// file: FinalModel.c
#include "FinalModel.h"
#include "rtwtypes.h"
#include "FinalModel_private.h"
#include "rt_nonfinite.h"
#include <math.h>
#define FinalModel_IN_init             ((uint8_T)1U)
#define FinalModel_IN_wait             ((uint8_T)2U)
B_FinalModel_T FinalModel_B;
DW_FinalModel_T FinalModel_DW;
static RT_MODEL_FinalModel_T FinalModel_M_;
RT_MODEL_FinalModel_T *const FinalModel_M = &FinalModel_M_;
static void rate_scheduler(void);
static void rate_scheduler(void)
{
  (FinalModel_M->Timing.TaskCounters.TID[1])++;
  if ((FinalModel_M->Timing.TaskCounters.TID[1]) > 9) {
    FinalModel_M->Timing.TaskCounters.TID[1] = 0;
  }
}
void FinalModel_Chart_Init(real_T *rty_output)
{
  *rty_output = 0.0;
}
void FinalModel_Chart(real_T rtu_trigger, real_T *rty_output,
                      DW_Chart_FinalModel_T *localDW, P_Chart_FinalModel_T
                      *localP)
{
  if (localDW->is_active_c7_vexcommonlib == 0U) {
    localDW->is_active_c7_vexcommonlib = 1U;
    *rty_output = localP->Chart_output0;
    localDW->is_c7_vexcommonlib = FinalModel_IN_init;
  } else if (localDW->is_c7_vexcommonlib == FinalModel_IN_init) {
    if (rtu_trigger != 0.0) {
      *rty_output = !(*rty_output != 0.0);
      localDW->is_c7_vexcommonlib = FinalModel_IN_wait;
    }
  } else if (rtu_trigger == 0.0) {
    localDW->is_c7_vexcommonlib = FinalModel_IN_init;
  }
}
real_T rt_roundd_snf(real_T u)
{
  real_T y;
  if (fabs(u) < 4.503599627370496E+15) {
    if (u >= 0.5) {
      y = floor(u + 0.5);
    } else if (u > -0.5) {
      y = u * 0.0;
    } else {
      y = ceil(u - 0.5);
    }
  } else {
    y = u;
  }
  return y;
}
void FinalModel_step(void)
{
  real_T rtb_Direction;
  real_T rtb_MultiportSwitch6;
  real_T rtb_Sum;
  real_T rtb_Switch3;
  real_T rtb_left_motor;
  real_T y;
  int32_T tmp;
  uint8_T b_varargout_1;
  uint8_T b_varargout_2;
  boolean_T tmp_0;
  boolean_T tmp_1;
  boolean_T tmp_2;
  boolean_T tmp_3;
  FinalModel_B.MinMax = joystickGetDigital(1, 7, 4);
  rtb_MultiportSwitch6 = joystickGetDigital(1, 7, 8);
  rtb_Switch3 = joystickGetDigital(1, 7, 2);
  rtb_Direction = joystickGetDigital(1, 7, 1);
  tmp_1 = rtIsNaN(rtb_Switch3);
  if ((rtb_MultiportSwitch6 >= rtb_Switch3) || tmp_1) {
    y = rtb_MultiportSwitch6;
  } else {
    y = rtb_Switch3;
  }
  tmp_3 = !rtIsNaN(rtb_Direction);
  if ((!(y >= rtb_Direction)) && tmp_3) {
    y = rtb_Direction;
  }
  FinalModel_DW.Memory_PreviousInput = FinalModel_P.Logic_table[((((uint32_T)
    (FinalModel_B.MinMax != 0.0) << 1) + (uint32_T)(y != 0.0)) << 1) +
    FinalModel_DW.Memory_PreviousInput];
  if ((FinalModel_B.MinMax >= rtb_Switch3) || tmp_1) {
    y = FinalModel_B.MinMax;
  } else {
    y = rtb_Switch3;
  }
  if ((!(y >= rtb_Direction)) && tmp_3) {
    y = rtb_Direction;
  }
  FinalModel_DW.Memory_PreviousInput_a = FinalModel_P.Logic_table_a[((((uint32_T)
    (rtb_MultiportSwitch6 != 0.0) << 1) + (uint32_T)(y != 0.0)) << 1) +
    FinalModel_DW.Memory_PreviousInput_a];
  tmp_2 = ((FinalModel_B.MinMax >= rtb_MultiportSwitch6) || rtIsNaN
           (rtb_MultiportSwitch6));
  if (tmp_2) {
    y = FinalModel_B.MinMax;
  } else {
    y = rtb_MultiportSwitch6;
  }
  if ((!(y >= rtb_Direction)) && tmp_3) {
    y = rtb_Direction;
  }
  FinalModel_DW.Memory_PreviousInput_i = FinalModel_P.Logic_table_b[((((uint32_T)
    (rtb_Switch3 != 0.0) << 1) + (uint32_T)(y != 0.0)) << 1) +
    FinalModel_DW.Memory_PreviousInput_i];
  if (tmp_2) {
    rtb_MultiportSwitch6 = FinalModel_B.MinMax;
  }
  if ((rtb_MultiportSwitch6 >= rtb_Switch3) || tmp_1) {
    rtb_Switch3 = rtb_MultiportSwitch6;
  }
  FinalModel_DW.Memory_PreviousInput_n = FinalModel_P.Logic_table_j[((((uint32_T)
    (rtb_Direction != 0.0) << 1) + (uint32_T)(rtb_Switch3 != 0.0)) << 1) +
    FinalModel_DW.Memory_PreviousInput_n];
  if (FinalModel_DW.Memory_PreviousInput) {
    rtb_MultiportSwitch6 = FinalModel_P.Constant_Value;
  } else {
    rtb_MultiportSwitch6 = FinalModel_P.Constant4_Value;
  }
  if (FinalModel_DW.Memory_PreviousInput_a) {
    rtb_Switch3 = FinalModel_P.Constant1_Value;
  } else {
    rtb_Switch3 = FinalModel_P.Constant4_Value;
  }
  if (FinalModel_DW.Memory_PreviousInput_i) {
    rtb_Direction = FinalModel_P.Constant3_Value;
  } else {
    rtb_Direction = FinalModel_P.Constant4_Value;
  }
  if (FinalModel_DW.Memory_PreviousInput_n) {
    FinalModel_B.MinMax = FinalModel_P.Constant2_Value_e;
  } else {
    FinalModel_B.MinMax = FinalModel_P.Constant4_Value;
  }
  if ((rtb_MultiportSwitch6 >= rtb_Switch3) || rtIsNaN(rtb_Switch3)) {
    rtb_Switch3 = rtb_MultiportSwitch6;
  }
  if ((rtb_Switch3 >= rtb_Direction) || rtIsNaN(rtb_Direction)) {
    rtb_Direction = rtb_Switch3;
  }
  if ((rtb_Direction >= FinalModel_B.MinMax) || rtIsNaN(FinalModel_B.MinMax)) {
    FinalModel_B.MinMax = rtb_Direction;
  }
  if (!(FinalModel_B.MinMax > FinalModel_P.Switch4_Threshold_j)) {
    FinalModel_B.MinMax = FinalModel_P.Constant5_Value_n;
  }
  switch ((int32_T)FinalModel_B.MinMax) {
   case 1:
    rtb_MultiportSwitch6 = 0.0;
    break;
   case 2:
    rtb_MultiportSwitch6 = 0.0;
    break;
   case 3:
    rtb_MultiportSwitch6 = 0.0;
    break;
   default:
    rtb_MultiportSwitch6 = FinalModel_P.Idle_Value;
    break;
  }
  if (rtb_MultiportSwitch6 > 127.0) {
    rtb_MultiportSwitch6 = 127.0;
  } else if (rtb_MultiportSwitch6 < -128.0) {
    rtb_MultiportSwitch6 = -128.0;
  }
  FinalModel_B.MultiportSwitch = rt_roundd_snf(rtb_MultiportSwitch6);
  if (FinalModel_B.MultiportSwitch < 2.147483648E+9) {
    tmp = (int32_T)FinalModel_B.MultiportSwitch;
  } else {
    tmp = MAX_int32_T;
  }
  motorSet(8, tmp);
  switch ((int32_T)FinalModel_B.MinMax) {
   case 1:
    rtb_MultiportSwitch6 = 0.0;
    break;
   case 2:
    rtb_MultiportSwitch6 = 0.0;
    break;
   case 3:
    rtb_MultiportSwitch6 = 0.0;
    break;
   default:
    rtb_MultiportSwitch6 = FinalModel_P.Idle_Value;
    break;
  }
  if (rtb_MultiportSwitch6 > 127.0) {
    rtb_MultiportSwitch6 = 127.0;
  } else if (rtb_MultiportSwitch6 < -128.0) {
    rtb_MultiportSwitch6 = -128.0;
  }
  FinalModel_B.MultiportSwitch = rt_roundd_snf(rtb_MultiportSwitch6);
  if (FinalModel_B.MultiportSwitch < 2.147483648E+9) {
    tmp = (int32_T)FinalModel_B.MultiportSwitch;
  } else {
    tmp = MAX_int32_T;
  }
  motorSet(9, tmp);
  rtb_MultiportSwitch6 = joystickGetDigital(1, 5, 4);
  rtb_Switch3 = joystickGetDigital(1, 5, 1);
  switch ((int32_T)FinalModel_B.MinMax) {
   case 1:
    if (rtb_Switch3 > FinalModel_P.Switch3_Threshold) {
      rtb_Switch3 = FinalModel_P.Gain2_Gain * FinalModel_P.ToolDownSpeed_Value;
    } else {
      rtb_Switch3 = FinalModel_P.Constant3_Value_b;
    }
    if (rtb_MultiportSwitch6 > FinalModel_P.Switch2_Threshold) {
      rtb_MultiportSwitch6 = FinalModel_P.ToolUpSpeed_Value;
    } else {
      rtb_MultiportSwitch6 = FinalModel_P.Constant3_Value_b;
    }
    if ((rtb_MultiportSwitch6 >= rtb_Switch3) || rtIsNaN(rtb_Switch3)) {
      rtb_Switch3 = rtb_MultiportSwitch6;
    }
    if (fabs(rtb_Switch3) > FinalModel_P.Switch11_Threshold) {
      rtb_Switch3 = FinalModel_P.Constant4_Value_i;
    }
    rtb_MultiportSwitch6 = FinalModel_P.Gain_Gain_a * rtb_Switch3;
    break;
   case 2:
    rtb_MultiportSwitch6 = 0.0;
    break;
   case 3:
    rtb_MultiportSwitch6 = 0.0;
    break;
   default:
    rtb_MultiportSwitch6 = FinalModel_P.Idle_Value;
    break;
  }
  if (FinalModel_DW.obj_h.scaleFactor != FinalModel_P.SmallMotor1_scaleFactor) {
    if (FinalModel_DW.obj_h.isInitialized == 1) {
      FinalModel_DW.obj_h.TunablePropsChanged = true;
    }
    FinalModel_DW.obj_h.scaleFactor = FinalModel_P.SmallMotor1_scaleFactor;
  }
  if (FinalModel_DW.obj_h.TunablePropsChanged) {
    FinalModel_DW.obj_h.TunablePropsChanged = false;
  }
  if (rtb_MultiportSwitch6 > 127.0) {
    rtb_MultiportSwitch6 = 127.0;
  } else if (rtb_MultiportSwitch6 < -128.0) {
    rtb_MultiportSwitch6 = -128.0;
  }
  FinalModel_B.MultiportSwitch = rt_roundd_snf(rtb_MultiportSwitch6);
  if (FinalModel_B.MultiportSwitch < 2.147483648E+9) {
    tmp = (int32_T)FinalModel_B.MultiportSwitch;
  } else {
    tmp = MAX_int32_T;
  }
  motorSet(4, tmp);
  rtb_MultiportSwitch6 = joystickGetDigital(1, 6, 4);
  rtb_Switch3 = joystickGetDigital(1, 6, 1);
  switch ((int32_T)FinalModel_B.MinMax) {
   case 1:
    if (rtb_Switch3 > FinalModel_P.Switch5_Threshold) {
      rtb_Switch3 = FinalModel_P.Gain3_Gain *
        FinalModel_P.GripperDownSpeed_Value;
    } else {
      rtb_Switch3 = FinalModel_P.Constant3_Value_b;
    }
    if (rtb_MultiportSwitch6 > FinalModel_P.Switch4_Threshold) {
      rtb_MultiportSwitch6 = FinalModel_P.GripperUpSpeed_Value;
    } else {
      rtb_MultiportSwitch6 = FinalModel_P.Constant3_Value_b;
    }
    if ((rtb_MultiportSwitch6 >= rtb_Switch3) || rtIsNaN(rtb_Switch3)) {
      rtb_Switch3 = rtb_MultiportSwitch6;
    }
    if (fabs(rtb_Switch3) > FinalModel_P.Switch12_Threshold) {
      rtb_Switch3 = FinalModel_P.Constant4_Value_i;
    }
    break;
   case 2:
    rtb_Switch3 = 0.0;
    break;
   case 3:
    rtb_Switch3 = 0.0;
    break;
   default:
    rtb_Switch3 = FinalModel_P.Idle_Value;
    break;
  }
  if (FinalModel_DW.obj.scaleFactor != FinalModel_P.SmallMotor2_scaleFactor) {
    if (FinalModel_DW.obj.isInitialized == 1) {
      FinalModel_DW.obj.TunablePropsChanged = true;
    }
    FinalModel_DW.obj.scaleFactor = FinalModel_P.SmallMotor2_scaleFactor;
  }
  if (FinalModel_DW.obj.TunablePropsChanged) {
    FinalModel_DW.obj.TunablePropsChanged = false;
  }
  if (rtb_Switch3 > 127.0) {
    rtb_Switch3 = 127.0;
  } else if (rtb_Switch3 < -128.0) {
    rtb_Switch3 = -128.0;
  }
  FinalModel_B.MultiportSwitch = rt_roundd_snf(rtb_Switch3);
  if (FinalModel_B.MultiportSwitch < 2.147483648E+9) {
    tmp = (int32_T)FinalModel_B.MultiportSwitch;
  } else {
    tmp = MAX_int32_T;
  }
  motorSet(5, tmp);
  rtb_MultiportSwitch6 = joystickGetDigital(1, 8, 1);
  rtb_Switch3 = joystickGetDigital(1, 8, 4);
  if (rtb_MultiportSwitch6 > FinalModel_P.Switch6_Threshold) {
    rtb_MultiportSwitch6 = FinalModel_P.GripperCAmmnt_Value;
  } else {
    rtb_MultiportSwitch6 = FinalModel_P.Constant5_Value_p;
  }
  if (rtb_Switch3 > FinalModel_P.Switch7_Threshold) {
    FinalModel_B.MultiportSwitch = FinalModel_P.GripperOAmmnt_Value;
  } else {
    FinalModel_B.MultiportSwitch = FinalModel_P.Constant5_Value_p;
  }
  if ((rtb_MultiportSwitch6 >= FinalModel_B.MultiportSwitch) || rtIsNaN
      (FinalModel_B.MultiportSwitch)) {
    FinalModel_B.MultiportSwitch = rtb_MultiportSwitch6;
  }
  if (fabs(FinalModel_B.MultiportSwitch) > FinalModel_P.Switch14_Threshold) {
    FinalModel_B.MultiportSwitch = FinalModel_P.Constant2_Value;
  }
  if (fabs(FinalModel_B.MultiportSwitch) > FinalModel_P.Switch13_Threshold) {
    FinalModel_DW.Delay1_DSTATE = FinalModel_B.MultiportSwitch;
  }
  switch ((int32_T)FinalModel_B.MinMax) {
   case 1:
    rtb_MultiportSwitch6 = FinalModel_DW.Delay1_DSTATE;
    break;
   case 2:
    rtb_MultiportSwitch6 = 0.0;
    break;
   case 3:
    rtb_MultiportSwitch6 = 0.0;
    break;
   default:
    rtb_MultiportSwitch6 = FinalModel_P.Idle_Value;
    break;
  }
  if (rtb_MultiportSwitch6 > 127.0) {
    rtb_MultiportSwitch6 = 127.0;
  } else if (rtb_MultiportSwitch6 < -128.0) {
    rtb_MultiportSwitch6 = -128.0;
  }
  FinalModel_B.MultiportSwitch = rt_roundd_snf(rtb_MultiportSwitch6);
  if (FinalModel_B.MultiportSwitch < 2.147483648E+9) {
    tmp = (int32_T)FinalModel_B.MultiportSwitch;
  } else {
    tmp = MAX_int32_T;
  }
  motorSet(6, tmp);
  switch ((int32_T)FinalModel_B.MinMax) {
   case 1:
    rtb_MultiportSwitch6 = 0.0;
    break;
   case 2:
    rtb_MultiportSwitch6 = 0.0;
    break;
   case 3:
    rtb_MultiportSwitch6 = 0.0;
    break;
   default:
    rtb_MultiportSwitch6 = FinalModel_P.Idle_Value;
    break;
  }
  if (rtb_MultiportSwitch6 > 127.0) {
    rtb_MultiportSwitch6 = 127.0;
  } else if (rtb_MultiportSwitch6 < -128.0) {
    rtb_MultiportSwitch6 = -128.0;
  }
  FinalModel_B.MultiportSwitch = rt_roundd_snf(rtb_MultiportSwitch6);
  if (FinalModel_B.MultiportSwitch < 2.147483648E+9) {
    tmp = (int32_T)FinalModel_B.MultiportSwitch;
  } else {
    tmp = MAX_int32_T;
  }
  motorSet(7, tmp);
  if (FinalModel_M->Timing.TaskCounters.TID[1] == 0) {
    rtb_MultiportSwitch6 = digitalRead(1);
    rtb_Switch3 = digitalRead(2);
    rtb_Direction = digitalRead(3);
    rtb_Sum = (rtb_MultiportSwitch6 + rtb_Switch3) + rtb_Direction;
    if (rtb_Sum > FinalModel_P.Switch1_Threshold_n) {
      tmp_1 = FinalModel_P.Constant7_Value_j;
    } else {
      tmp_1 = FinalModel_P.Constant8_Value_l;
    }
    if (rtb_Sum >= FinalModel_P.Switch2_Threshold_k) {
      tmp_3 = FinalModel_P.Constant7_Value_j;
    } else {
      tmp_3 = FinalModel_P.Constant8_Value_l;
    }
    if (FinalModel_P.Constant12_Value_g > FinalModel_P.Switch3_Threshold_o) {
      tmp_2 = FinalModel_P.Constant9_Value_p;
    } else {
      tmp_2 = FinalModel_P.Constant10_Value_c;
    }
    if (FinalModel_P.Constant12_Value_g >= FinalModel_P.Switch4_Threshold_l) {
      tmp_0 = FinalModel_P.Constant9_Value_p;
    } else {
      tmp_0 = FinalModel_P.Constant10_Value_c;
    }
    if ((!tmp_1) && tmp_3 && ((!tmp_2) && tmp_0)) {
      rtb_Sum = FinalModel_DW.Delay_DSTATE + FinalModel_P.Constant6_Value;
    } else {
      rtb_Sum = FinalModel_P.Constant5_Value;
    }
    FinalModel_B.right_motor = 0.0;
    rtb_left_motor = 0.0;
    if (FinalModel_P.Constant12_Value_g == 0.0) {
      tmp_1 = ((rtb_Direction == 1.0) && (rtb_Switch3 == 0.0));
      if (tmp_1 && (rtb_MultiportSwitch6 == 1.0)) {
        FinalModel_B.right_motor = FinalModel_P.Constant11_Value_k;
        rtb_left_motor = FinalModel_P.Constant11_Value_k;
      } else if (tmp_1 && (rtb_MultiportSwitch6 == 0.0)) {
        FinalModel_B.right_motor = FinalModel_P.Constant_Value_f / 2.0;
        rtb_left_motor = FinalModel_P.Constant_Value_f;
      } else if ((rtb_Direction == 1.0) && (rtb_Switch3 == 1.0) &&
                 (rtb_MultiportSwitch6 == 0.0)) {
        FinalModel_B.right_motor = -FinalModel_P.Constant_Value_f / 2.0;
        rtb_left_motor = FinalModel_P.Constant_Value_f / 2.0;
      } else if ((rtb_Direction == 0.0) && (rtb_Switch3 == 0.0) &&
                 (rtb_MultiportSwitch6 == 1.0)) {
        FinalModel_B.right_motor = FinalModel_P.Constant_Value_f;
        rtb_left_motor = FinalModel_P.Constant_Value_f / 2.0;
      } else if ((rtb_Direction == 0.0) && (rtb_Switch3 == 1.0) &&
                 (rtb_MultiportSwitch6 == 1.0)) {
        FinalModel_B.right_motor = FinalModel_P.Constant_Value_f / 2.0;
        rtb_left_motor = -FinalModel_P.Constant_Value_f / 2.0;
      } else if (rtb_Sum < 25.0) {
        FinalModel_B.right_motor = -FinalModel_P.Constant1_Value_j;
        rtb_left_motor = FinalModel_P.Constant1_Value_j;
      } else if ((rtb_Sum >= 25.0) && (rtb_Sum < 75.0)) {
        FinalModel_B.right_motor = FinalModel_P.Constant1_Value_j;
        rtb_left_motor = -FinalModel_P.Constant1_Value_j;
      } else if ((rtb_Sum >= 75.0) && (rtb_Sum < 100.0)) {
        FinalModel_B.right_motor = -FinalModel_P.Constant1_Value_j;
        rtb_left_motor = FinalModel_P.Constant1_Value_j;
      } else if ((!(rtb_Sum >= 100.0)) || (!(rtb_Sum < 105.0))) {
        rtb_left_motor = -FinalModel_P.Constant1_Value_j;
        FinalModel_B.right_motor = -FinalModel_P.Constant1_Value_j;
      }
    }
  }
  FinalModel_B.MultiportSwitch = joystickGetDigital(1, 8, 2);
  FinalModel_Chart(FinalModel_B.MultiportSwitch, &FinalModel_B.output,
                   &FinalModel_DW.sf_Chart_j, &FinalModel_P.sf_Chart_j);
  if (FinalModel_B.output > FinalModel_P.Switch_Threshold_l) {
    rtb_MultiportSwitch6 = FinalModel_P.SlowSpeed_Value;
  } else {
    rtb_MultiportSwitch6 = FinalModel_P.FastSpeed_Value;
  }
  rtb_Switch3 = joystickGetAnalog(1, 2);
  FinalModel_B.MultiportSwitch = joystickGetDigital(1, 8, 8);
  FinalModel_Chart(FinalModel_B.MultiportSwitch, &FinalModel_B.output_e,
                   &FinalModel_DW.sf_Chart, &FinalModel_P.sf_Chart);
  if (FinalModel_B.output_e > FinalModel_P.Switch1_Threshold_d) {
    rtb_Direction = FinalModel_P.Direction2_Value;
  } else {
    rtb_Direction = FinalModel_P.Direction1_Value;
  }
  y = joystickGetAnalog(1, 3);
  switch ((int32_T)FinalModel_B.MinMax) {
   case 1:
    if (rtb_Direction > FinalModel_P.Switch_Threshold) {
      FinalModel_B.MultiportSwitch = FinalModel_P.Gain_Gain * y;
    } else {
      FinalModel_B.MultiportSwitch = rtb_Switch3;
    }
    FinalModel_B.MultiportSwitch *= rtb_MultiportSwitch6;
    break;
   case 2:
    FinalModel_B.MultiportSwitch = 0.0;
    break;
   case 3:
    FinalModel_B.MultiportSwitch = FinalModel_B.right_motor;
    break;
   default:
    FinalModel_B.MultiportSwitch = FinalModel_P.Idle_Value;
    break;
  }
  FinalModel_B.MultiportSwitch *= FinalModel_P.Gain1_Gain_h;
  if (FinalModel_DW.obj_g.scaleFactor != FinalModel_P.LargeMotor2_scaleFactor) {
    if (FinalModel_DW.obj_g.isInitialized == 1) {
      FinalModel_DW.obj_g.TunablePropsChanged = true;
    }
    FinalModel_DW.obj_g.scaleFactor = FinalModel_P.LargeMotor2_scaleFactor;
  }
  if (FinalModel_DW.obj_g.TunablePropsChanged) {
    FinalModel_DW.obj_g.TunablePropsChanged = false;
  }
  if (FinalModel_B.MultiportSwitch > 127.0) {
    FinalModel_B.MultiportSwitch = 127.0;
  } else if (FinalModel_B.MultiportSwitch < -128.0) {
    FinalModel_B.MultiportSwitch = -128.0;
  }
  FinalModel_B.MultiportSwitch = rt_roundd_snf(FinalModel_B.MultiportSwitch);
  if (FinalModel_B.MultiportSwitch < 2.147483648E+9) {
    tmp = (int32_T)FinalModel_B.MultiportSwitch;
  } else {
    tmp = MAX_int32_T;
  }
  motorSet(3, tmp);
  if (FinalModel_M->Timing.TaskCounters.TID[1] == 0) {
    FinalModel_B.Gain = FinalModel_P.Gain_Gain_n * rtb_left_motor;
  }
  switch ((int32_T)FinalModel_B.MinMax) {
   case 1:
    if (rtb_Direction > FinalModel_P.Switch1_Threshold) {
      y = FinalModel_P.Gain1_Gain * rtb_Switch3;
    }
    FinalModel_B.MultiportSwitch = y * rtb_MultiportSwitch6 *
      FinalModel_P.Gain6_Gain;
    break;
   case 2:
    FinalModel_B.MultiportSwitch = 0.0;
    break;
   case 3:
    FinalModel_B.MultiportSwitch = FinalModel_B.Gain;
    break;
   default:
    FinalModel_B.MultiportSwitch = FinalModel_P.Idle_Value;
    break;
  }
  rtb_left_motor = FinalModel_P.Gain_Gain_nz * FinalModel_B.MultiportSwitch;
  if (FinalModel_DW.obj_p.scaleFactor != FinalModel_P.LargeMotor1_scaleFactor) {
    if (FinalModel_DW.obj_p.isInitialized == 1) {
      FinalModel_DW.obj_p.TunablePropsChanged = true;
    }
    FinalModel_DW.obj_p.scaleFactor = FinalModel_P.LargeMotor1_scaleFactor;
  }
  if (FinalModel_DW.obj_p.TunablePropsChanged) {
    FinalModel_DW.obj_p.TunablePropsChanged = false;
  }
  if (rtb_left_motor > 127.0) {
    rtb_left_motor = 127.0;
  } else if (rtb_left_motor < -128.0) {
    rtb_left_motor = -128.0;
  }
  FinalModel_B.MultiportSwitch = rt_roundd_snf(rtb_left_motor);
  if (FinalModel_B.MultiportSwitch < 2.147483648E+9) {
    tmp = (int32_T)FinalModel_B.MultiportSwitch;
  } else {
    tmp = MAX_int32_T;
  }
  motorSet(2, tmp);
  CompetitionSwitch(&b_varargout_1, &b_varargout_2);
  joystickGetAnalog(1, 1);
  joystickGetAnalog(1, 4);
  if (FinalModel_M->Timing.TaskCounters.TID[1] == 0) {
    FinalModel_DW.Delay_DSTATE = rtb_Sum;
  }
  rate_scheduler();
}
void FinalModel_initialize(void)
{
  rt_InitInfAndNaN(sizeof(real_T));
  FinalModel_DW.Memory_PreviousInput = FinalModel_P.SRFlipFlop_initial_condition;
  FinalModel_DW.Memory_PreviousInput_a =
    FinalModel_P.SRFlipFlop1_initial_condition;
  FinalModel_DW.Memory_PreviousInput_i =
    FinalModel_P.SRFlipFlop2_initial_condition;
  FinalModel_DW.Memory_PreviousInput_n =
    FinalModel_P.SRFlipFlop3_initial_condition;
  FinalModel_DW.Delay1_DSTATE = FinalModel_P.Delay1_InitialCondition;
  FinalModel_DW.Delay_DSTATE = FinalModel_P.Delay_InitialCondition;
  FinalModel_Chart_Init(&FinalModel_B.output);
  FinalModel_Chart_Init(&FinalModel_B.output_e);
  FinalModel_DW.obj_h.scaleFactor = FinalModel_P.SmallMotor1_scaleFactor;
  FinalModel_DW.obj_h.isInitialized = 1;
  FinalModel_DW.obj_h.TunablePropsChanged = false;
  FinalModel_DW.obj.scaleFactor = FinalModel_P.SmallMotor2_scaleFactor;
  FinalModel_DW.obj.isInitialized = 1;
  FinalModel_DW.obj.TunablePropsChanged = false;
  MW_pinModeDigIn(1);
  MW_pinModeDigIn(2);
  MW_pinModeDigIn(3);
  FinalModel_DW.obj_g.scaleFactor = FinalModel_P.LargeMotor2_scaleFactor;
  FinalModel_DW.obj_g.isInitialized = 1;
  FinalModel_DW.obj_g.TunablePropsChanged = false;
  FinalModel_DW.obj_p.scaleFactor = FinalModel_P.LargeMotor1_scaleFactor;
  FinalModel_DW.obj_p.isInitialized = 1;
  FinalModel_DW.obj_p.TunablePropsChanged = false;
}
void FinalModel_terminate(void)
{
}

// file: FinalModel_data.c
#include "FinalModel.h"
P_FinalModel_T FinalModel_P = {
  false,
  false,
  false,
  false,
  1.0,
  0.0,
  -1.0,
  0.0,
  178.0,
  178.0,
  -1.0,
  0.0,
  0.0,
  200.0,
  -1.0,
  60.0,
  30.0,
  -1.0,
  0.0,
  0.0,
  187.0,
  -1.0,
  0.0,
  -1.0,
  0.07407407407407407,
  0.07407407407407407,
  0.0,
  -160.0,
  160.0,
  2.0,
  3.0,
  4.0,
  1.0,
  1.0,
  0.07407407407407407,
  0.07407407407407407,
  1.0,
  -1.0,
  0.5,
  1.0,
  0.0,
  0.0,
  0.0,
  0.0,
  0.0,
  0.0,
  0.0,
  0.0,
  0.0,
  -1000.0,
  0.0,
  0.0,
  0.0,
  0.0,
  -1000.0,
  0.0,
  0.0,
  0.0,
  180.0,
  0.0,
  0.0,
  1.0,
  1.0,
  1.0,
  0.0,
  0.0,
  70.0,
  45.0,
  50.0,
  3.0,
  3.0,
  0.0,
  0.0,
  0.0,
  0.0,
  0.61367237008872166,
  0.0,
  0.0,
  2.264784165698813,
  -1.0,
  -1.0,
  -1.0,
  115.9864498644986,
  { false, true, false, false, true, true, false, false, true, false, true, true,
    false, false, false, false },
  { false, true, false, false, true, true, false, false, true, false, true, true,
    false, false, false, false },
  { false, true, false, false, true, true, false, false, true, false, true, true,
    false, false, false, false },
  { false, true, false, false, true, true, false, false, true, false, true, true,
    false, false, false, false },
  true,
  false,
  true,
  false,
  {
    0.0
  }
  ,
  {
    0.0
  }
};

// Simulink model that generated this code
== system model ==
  ServoMotor#1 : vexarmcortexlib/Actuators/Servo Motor  <- 1: MultiportSwitch6
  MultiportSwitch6 : MultiPortSwitch  Inputs=4  <- 1: Switch4, 5: Idle
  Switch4 : Switch  Criteria=u2 > Threshold  <- 1: MinMax, 2: MinMax, 3: Constant5
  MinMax : MinMax  Function=max  Inputs=4  <- 1: Switch, 2: Switch1, 3: Switch2, 4: Switch3
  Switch : Switch  Criteria=u2 > Threshold  <- 1: Constant, 2: SRFlipFlop, 3: Constant4
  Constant : Constant
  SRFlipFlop : simulink_extras/Flip Flops/S-R Flip-Flop  <- 1: DataTypeConversion#1, 2: DataTypeConversion#2
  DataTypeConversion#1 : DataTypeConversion  <- 1: GamepadButton#1
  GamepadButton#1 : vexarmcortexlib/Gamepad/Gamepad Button  <- 1: Constant#1
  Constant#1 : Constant  Value=0
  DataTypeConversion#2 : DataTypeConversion  <- 1: MinMax#1
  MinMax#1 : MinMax  Function=max  Inputs=3  <- 1: GamepadButton#2, 2: GamepadButton#3, 3: GamepadButton#4
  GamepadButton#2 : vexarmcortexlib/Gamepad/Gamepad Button  <- 1: Constant1
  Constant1 : Constant  Value=0
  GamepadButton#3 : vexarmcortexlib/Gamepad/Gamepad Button  <- 1: Constant2
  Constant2 : Constant  Value=0
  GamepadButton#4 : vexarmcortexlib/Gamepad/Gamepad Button  <- 1: Constant3
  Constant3 : Constant  Value=0
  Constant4 : Constant  Value=0
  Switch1 : Switch  Criteria=u2 > Threshold  <- 1: Constant#2, 2: SRFlipFlop1, 3: Constant4
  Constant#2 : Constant  Value=2
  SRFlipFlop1 : simulink_extras/Flip Flops/S-R Flip-Flop  <- 1: DataTypeConversion#3, 2: DataTypeConversion#4
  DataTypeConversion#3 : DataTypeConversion  <- 1: GamepadButton#2
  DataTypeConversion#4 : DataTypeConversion  <- 1: MinMax#2
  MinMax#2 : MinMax  Function=max  Inputs=3  <- 1: GamepadButton#1, 2: GamepadButton#3, 3: GamepadButton#4
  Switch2 : Switch  Criteria=u2 > Threshold  <- 1: Constant#3, 2: SRFlipFlop2, 3: Constant4
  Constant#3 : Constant  Value=3
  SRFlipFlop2 : simulink_extras/Flip Flops/S-R Flip-Flop  <- 1: DataTypeConversion#5, 2: DataTypeConversion#6
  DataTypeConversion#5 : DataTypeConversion  <- 1: GamepadButton#3
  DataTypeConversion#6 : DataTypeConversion  <- 1: MinMax#3
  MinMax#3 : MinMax  Function=max  Inputs=3  <- 1: GamepadButton#1, 2: GamepadButton#2, 3: GamepadButton#4
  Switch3 : Switch  Criteria=u2 > Threshold  <- 1: Constant#4, 2: SRFlipFlop3, 3: Constant4
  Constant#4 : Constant  Value=4
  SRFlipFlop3 : simulink_extras/Flip Flops/S-R Flip-Flop  <- 1: DataTypeConversion#7, 2: DataTypeConversion#8
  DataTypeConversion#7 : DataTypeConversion  <- 1: GamepadButton#4
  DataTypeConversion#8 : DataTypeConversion  <- 1: MinMax#4
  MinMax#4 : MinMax  Function=max  Inputs=3  <- 1: GamepadButton#1, 2: GamepadButton#2, 3: GamepadButton#3
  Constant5 : Constant
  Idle : Constant  Value=0
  ServoMotor#2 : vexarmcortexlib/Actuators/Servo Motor  <- 1: MultiPortSwitch#1
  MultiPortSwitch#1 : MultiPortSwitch  Inputs=4  <- 1: Switch4, 5: Idle
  SmallMotor1 : vexarmcortexlib/Actuators/DC Motor  <- 1: MultiPortSwitch#2
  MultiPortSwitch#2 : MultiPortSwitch  Inputs=4  <- 1: Switch4, 2: Gain, 5: Idle
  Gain : Gain  Gain=-1  <- 1: Switch11
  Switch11 : Switch  Criteria=u2 > Threshold  Threshold=200  <- 1: Constant#5, 2: Abs#1, 3: MinMax#5
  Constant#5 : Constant  Value=0
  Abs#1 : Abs  <- 1: MinMax#5
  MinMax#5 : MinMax  Function=max  Inputs=2  <- 1: Switch#1, 2: Switch#2
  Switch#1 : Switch  Criteria=u2 > Threshold  <- 1: ToolUpSpeed, 2: GamepadButton#5, 3: Constant#6
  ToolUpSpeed : Constant  Value=178
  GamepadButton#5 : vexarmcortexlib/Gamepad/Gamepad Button  <- 1: Constant11
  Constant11 : Constant  Value=0
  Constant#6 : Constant  Value=-1000
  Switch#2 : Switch  Criteria=u2 > Threshold  <- 1: Gain2, 2: GamepadButton#6, 3: Constant#6
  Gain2 : Gain  Gain=-1  <- 1: ToolDownSpeed
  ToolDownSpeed : Constant  Value=178
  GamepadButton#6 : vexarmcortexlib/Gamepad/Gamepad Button  <- 1: Constant12
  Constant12 : Constant  Value=0
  SmallMotor2 : vexarmcortexlib/Actuators/DC Motor  <- 1: MultiPortSwitch#3
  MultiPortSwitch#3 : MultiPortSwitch  Inputs=4  <- 1: Switch4, 2: Switch12, 5: Idle
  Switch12 : Switch  Criteria=u2 > Threshold  Threshold=187  <- 1: Constant#5, 2: Abs#2, 3: MinMax#6
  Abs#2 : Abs  <- 1: MinMax#6
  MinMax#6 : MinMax  Function=max  Inputs=2  <- 1: Switch#3, 2: Switch5
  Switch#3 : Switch  Criteria=u2 > Threshold  <- 1: GripperUpSpeed, 2: GamepadButton#7, 3: Constant#6
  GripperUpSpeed : Constant  Value=60
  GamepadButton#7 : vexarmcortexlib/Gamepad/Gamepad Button  <- 1: Constant#7
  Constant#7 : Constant  Value=0
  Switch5 : Switch  Criteria=u2 > Threshold  <- 1: Gain3, 2: GamepadButton#8, 3: Constant#6
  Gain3 : Gain  Gain=-1  <- 1: GripperDownSpeed
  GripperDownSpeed : Constant  Value=30
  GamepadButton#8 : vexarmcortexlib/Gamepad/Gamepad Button  <- 1: Constant#8
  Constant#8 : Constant  Value=0
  ServoMotor#3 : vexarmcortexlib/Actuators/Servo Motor  <- 1: MultiPortSwitch#4
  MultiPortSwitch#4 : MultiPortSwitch  Inputs=4  <- 1: Switch4, 2: Switch13, 5: Idle
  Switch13 : Switch  Criteria=u2 > Threshold  <- 1: Switch14, 2: Abs#3, 3: Delay1
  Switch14 : Switch  Criteria=u2 > Threshold  Threshold=180  <- 1: Constant#9, 2: Abs#4, 3: MinMax#7
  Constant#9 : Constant  Value=0
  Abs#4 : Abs  <- 1: MinMax#7
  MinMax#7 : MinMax  Function=max  Inputs=2  <- 1: Switch6, 2: Switch7
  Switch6 : Switch  Criteria=u2 > Threshold  <- 1: GripperCAmmnt, 2: GamepadButton#9, 3: Constant#10
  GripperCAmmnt : Constant  Value=-160
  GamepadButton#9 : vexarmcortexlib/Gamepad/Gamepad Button  <- 1: Constant8
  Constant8 : Constant  Value=0
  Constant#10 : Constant  Value=-1000
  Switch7 : Switch  Criteria=u2 > Threshold  <- 1: GripperOAmmnt, 2: GamepadButton#10, 3: Constant#10
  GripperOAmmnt : Constant  Value=160
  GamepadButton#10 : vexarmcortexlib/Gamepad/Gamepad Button  <- 1: Constant9
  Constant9 : Constant  Value=0
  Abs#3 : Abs  <- 1: Switch14
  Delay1 : Delay  DelayLength=1  <- 1: Switch13
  ServoMotor#4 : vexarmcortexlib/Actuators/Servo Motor  <- 1: MultiPortSwitch#5
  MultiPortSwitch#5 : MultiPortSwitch  Inputs=4  <- 1: Switch4, 5: Idle
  Product#1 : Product  <- 1: Switch#4
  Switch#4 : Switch  Criteria=u2 > Threshold  <- 1: Gain#1
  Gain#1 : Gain  Gain=-1
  LargeMotor2 : vexarmcortexlib/Actuators/DC Motor  <- 1: Gain1
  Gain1 : Gain  Gain=-1  <- 1: MultiPortSwitch#6
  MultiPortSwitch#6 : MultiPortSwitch  Inputs=4  <- 1: Switch4, 2: Product#2, 4: MATLABFunction#1, 5: Idle
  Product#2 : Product  <- 1: Switch#5, 2: Switch#6
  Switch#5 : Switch  Criteria=u2 > Threshold  <- 1: Gain#2, 2: Switch#7, 3: GamepadJoystick#1
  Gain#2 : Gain  Gain=-1  <- 1: GamepadJoystick#2
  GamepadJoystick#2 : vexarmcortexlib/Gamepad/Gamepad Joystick  <- 1: Constant7
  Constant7 : Constant  Value=2.264784165698813
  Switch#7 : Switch  Criteria=u2 > Threshold  <- 1: Direction2, 2: Direction, 3: Direction1
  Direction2 : Constant
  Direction : vexcommonlib/Latch  <- 1: GamepadButton#11
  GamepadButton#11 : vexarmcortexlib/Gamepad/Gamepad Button  <- 1: Constant#11
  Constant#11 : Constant  Value=0
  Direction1 : Constant  Value=-1
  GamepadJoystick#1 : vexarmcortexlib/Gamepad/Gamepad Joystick  <- 1: Constant6
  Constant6 : Constant  Value=0.6136723700887217
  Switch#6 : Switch  Criteria=u2 > Threshold  <- 1: SlowSpeed, 2: Latch#1, 3: FastSpeed
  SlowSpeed : Constant  Value=0.5
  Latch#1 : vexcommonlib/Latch  <- 1: GamepadButton#12
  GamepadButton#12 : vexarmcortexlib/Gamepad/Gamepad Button  <- 1: Constant#12
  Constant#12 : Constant  Value=0
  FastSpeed : Constant
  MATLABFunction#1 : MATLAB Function  <- 1: DigitalInput#1, 2: DigitalInput#2, 3: DigitalInput#3, 4: Constant#13, 5: Constant#14, 6: Constant#15, 7: Switch#8, 8: Constant#16
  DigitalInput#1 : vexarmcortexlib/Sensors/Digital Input  <- 1: Constant#17
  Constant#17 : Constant
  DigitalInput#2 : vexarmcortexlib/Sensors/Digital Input  <- 1: Constant#18
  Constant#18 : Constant
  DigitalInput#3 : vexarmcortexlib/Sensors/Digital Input  <- 1: Constant#19
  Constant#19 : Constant
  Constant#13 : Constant  Value=0
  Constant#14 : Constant  Value=70
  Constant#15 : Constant  Value=45
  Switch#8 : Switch  Criteria=u2 > Threshold  <- 1: Sum#1, 2: Logic#1, 3: Constant#20
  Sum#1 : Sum  <- 1: Delay, 2: Constant#21
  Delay : Delay  DelayLength=1  <- 1: Switch#8
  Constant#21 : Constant
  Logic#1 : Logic  <- 1: Logic#2, 2: Logic#3
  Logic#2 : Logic  <- 1: Logic#4, 2: Switch#9
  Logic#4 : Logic  Operator=NOT  <- 1: Switch#10
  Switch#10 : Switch  Criteria=u2 > Threshold  Threshold=3  <- 1: Constant#22, 2: Sum, 3: Constant#23
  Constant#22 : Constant  Value=true
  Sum : Sum  Inputs=+++  <- 1: DigitalInput#1, 2: DigitalInput#2, 3: DigitalInput#3
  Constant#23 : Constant  Value=false
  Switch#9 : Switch  Threshold=3  <- 1: Constant#22, 2: Sum, 3: Constant#23
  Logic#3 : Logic  <- 1: Logic#5, 2: Switch#11
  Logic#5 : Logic  Operator=NOT  <- 1: Switch#12
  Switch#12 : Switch  Criteria=u2 > Threshold  <- 1: Constant#24, 2: Constant#13, 3: Constant10
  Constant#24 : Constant  Value=true
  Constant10 : Constant  Value=false
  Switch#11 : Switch  <- 1: Constant#24, 2: Constant#13, 3: Constant10
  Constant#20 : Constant  Value=0
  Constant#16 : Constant  Value=50
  Gain6 : Gain  Gain=-1  <- 1: Product#3
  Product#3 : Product  <- 1: Switch#13
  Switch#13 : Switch  Criteria=u2 > Threshold  <- 1: Gain#3
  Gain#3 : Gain  Gain=-1
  LargeMotor1 : vexarmcortexlib/Actuators/DC Motor  <- 1: Gain#4
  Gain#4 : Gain  Gain=-1  <- 1: MultiportSwitch
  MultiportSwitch : MultiPortSwitch  Inputs=4  <- 1: Switch4, 2: Gain#5, 4: Gain#6, 5: Idle
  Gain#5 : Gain  Gain=-1  <- 1: Product#4
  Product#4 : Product  <- 1: Switch#14, 2: Switch#6
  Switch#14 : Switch  Criteria=u2 > Threshold  <- 1: Gain#7, 2: Switch#7, 3: GamepadJoystick#2
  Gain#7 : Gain  Gain=-1  <- 1: GamepadJoystick#1
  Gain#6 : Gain  Gain=-1  <- 1: MATLABFunction#1/2
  CompetitionSwitch : vexarmcortexlib/Gamepad/Competition Switch
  GamepadJoystick#3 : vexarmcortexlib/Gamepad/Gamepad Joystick  <- 1: Constant#25
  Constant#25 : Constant  Value=115.9864498644986
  GamepadJoystick#4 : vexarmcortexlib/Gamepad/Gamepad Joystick
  CustomTuningWebBlock#1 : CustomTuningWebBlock
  CustomTuningWebBlock#2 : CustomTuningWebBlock
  CustomTuningWebBlock#3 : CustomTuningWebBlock
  CustomTuningWebBlock#4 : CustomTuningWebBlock
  CustomTuningWebBlock#5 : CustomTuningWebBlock
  CustomTuningWebBlock#6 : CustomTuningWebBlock
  CustomTuningWebBlock#7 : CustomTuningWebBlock
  CustomTuningWebBlock#8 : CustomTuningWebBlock
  CustomTuningWebBlock#9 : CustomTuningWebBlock
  CustomTuningWebBlock#10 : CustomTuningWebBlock
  CustomTuningWebBlock#11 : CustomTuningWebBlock
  CustomTuningWebBlock#12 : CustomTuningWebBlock
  CustomTuningWebBlock#13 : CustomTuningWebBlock
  RockerSwitchBlock#1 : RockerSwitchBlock
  CustomTuningWebBlock#14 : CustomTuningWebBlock
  CustomTuningWebBlock#15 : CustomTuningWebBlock
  CustomTuningWebBlock#16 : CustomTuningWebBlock
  CustomTuningWebBlock#17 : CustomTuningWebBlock
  CustomTuningWebBlock#18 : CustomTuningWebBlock
== matlab function MATLABFunction#1 ==
function [right_motor, left_motor, time]  = line_follow(right, middle, left, mode, speed, scanspeed, time, straightspeed)
right_motor = 0;
left_motor = 0;
if mode == 0
   if left == 1 && middle == 0 && right == 1
       %Straight
       right_motor = straightspeed;
       left_motor = straightspeed;
   elseif left == 1 && middle == 0 && right == 0
       %RightSlight
       right_motor = speed/2;
       left_motor = speed;
   elseif left == 1 && middle == 1 && right == 0
       %Right
       right_motor = -speed/2;
       left_motor = speed/2;
   elseif left == 0 && middle == 0 && right == 1
       %LeftSlight
       right_motor = speed;
       left_motor = speed/2;
   elseif left == 0 && middle == 1 && right == 1
       %Left
       right_motor = speed/2;
       left_motor = -speed/2;
   else     %scanning
       if time < 25 %change to time off
           %scan right
           right_motor = -scanspeed;
           left_motor = scanspeed;
       elseif time >= 25 && time < 75 %change to time off
           %scan left
           right_motor = scanspeed;
           left_motor = -scanspeed;
       elseif time >= 75 && time < 100  %change to time off
           right_motor = -scanspeed;
           left_motor = scanspeed;
       elseif time >= 100 && time < 105  %change to time off
           right_motor = 0;
           left_motor = 0;           
       else
           left_motor = -scanspeed;
           right_motor = -scanspeed;
       end
   end
end
